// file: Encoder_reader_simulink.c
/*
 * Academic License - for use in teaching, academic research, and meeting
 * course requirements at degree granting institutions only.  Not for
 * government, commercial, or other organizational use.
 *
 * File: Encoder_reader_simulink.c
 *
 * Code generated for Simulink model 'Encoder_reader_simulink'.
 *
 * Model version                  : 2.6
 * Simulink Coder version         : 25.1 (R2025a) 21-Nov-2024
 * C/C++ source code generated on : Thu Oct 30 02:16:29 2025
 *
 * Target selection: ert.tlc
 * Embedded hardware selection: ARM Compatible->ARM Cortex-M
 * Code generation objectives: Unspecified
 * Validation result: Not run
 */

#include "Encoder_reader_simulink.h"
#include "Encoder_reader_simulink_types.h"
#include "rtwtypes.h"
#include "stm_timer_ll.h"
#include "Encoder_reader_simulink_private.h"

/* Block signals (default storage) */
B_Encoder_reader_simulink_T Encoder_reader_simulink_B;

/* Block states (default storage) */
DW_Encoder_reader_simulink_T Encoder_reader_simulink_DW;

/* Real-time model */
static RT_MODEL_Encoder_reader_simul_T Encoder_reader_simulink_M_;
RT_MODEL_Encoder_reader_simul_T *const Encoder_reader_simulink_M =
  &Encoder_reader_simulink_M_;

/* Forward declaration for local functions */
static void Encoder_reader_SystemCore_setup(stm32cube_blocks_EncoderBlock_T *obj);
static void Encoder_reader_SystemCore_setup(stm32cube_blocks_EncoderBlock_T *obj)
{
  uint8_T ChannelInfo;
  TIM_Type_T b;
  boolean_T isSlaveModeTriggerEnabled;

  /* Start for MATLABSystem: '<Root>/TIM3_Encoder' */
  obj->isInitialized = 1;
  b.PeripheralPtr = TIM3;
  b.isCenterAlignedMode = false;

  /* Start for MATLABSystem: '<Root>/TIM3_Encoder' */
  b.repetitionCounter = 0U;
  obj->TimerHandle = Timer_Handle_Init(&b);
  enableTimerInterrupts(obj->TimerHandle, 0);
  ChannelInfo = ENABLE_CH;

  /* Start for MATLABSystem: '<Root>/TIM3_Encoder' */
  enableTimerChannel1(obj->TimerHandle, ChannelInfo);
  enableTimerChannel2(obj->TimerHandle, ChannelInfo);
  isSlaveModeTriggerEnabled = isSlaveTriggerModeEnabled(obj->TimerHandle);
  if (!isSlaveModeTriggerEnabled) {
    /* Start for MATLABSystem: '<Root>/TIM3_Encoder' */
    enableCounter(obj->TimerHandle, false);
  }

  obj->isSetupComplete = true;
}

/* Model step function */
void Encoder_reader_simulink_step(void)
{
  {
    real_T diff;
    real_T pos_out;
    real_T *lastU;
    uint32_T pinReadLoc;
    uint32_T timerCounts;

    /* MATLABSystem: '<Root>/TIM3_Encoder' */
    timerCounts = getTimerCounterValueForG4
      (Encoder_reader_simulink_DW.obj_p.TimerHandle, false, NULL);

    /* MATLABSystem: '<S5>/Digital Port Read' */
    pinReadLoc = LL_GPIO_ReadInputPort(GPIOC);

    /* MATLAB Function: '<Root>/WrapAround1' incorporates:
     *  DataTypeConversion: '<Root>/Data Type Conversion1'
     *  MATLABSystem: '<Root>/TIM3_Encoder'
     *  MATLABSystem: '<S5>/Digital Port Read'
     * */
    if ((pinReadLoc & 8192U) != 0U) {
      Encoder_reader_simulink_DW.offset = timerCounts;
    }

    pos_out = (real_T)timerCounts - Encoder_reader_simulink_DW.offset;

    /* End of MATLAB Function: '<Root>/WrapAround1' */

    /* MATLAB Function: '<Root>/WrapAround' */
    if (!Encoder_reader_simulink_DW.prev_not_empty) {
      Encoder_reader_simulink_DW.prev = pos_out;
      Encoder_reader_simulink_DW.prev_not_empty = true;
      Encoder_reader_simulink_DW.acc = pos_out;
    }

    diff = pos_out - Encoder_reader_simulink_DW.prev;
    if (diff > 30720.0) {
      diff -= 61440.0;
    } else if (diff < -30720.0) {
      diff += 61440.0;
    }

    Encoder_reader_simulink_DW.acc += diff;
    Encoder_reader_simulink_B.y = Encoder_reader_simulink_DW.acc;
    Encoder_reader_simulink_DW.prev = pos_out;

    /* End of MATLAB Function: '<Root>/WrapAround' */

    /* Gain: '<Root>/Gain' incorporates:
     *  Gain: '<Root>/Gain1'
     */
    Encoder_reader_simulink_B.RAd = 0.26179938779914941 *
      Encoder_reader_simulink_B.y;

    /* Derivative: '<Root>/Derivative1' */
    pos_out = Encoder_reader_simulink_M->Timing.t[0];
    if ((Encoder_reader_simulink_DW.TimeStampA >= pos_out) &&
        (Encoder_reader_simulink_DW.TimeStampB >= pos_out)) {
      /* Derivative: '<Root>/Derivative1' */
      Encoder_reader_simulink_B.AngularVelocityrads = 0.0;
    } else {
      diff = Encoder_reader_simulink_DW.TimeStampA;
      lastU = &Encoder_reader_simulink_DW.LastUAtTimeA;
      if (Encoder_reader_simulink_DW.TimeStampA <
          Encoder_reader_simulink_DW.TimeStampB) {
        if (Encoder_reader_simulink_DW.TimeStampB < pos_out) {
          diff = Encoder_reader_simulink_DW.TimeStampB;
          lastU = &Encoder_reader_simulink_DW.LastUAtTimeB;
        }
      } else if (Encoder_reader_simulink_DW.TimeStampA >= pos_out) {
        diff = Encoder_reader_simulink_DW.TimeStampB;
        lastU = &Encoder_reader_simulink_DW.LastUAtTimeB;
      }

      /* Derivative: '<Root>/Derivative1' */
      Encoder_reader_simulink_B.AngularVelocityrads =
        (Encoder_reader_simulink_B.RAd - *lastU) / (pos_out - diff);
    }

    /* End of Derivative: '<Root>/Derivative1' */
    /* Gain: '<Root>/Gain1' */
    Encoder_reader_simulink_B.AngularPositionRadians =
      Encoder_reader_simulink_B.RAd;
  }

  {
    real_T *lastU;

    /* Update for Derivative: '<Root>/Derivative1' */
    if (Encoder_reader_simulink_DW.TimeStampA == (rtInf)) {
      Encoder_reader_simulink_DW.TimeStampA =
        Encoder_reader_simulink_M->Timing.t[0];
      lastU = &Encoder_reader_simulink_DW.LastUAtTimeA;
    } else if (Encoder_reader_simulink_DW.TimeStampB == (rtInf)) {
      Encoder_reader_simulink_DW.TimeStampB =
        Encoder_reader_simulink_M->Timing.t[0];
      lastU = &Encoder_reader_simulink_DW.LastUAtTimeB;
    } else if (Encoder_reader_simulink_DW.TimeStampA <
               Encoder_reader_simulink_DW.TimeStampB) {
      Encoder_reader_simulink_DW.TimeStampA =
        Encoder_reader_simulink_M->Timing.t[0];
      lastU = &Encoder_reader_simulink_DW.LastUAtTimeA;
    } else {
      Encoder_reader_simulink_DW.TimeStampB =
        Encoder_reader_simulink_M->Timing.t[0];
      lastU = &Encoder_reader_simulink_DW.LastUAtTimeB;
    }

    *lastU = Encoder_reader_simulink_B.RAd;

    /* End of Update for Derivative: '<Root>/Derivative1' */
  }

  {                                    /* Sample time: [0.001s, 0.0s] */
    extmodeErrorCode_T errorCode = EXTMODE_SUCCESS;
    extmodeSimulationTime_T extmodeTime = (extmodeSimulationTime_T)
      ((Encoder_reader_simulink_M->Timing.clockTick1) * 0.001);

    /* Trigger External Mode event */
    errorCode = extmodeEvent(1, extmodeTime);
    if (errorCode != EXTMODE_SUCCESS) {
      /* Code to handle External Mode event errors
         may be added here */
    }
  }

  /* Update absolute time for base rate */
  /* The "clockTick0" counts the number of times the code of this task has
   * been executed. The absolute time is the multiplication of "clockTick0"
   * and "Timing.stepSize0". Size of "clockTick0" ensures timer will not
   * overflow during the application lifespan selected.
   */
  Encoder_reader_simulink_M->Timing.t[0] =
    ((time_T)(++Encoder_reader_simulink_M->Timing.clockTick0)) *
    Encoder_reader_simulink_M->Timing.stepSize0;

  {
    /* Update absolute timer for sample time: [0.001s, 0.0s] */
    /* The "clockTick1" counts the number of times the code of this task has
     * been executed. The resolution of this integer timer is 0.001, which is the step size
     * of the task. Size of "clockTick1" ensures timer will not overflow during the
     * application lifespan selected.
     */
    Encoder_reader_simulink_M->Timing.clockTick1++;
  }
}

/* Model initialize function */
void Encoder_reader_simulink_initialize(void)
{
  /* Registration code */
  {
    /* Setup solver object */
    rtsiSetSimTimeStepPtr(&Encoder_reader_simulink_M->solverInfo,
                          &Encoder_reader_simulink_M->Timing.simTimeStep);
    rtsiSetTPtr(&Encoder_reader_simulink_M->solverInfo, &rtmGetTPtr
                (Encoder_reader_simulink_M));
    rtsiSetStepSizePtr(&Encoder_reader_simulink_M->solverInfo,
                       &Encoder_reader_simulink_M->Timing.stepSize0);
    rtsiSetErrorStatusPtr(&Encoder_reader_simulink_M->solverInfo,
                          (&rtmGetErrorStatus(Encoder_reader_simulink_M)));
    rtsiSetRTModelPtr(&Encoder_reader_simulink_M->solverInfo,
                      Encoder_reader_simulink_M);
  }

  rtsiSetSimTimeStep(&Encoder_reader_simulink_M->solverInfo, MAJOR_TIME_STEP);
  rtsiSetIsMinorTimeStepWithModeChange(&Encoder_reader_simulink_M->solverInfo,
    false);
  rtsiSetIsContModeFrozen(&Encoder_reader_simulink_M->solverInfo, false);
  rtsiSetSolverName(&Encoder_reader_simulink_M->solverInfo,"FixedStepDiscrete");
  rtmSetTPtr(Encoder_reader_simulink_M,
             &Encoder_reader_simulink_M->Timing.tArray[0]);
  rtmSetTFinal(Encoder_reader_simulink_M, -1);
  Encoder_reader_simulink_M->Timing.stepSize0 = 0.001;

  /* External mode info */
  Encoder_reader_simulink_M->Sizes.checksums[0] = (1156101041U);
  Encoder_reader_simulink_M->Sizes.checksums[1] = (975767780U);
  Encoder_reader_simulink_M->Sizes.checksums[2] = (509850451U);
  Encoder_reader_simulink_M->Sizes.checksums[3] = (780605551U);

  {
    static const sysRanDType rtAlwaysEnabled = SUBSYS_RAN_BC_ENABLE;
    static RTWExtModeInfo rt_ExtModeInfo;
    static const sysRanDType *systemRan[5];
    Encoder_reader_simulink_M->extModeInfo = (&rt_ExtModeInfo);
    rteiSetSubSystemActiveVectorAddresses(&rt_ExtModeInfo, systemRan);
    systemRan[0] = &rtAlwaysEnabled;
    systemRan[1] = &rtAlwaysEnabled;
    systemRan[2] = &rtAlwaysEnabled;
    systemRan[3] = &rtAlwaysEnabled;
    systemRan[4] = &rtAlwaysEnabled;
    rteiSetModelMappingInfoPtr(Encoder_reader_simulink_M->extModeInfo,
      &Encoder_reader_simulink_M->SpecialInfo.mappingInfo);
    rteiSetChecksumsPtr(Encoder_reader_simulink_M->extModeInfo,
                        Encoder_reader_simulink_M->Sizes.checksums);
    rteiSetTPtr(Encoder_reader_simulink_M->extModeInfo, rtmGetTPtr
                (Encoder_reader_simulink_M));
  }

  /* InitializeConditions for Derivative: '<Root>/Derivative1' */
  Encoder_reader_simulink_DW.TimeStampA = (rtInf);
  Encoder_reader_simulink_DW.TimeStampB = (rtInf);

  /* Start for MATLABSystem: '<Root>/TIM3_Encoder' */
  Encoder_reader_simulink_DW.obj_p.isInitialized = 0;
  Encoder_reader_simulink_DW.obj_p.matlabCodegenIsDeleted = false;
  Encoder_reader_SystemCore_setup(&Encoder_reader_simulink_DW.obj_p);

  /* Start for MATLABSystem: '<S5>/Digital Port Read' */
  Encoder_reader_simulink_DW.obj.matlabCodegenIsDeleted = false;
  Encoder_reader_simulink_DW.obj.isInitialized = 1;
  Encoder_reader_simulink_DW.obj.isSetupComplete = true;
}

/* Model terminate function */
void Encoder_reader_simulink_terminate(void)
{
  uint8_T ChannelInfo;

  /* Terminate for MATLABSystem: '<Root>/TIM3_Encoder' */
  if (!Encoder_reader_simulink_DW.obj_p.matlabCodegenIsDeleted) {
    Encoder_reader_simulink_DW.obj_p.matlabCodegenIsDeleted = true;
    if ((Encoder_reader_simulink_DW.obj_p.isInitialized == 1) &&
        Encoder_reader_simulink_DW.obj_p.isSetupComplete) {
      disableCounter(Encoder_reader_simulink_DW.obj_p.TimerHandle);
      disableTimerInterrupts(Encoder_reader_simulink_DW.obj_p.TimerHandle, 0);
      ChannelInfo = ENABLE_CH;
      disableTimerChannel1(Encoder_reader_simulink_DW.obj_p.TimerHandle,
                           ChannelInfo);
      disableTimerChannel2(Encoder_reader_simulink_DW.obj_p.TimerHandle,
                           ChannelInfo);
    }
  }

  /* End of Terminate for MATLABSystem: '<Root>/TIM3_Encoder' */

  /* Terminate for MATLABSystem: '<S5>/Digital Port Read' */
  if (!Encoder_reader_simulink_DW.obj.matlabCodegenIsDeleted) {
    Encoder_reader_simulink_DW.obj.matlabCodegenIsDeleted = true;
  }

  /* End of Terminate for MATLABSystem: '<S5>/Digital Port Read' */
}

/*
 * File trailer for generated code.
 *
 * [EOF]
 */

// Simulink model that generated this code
simulink model "Encoder_reader_simulink"  (R2025a)
settings: Solver=FixedStepAuto  StartTime=0.0  StopTime=inf  FixedStep=0.001  RelTol=1e-3  EnableMultiTasking=on
libraries: stm32f4xxblockslib x5, stm32g4xxblockslib x3

== system Encoder_reader_simulink ==
  Constant : Constant  Commented=on  Value=1.5
  Data Type Conversion1 : DataTypeConversion  OutDataTypeStr=double  SaturateOnIntegerOverflow=off  RndMeth=Floor
  Data Type Conversion2 : DataTypeConversion  Commented=on  OutDataTypeStr=double  SaturateOnIntegerOverflow=off  RndMeth=Floor
  Data Type Conversion3 : DataTypeConversion  Commented=on  OutDataTypeStr=double  SaturateOnIntegerOverflow=off  RndMeth=Floor
  Derivative1 : Derivative
  Digital Port Read1 : stm32f4xxblockslib/Digital Port Read  Commented=on  PortName=GPIOC  PinNumber=13  ReadOperation=on  IOAsArray=on  SampleTime=-1  EnableSimPort=off  hoistedMaskSrc=ECSoC/ECSimCodegen/Digital Port Read
  Digital Port Read2 : stm32f4xxblockslib/Digital Port Read  PortName=GPIOC  PinNumber=13  ReadOperation=on  IOAsArray=on  SampleTime=-1  EnableSimPort=off  hoistedMaskSrc=ECSoC/ECSimCodegen/Digital Port Read
  Digital Port Read3 : stm32f4xxblockslib/Digital Port Read  Commented=on  PortName=GPIOA  PinNumber=4  ReadOperation=on  IOAsArray=on  SampleTime=-1  EnableSimPort=off  hoistedMaskSrc=ECSoC/ECSimCodegen/Digital Port Read
  Digital Port Read4 : stm32f4xxblockslib/Digital Port Read  Commented=on  PortName=GPIOA  PinNumber=6  ReadOperation=on  IOAsArray=on  SampleTime=-1  EnableSimPort=off  hoistedMaskSrc=ECSoC/ECSimCodegen/Digital Port Read
  Digital Port Read5 : stm32f4xxblockslib/Digital Port Read  Commented=on  PortName=GPIOC  PinNumber=13  ReadOperation=on  IOAsArray=on  SampleTime=-1  EnableSimPort=off  hoistedMaskSrc=ECSoC/ECSimCodegen/Digital Port Read
  Display : Display
  Display{1..4} (4 alike) : Display  Commented=on
  Display5 : Display
  Display6 : Display
  Encoder : stm32g4xxblockslib/Encoder  Commented=on  TimerModule=TIM4  EnableResetInput=off  OutputCountAfterFirstIndex=off  OutputValidIndex=off  OutputDirection=off  OutputStatus=off  SampleTime=-1
  Gain : Gain  Gain=(2*pi)/24
  Gain1 : Gain  Gain=(2*pi)/24
  Sum : Sum  Commented=on  Inputs=|++
  TIM3_Encoder : stm32g4xxblockslib/Encoder  TimerModule=TIM3  EnableResetInput=off  OutputCountAfterFirstIndex=off  OutputValidIndex=off  OutputDirection=off  OutputStatus=off  SampleTime=-1
  TIM3_Encoder2 : stm32g4xxblockslib/Encoder  Commented=on  TimerModule=TIM1  EnableResetInput=off  OutputCountAfterFirstIndex=off  OutputValidIndex=off  OutputDirection=off  OutputStatus=off  SampleTime=-1
  WrapAround : MATLAB Function  TreatAsAtomicUnit=on
  WrapAround1 : MATLAB Function  TreatAsAtomicUnit=on
  WrapAround2 : MATLAB Function  Commented=on  TreatAsAtomicUnit=on
  WrapAround3 : MATLAB Function  Commented=on  TreatAsAtomicUnit=on
  WrapAround4 : MATLAB Function  Commented=on  TreatAsAtomicUnit=on
  WrapAround5 : MATLAB Function  Commented=on  TreatAsAtomicUnit=on
  wires:
  TIM3_Encoder/1 -> Data Type Conversion1/1
  WrapAround1/1(pos_out) -> WrapAround/1(u)
  Digital Port Read2/1 -> WrapAround1/2(home_btn)  "B"
  Data Type Conversion1/1 -> WrapAround1/1(pos_in)
  Data Type Conversion2/1 -> WrapAround3/1(pos_in)
  Digital Port Read1/1 -> WrapAround3/2(home_btn)  "B"
  WrapAround3/1(pos_out) -> WrapAround2/1(u)
  WrapAround2/1(y) -> Display1/1
  Encoder/1 -> Data Type Conversion2/1
  Digital Port Read3/1 -> Display2/1  "B"
  TIM3_Encoder2/1 -> Data Type Conversion3/1
  WrapAround4/1(y) -> Display4/1
  WrapAround5/1(pos_out) -> WrapAround4/1(u)
  Digital Port Read5/1 -> WrapAround5/2(home_btn)  "B"
  Data Type Conversion3/1 -> WrapAround5/1(pos_in)
  Digital Port Read4/1 -> Sum/1  "A"
  Constant/1 -> Sum/2
  Sum/1 -> Display3/1  "A"
  WrapAround/1(y) -> Display6/1, Gain1/1, Gain/1  "Relative Position (Pulses)"
  Gain/1 -> Derivative1/1  "RAd"
  Derivative1/1 -> Display/1  "Angular Velocity (rad/s)"
  Gain1/1 -> Display5/1  "Angular Position (Radians)"

== matlab function Encoder_reader_simulink/WrapAround1 ==
function pos_out = encoder_home(pos_in, home_btn)
%#codegen

persistent offset
if isempty(offset)
    offset = 0;  % ค่าเริ่มต้นของ offset
end

if home_btn == 1
    % เมื่อกดปุ่ม home ให้จำค่าปัจจุบันเป็น offset
    offset = pos_in;
end

% เอาค่าปัจจุบันลบด้วย offset → ให้ค่าเป็น 0 ที่ home
pos_out = pos_in - offset;

end

== matlab function Encoder_reader_simulink/WrapAround ==
function y = WrapAroundFcn(u)

persistent prev acc
if isempty(prev)
    prev = double(u);
    acc  = double(u);
end

wrapMax  = 61440;      % ค่า Period + 1 (61439 + 1)
halfWrap = wrapMax / 2;

% คำนวณความต่างระหว่างค่าปัจจุบันกับค่าก่อนหน้า
diff = double(u) - prev;

% ---------- ปรับค่าเมื่อข้ามรอบ ----------
if diff >  halfWrap
    % ข้ามจาก 61439 → 0  (CW)
    diff = diff - wrapMax;
elseif diff < -halfWrap
    % ข้ามจาก 0 → 61439  (CCW)
    diff = diff + wrapMax;
end

% ---------- สะสมค่าต่อเนื่อง ----------
acc = acc + diff;

% ---------- อัปเดตค่าและส่งออก ----------
y = acc;
prev = double(u);
end

== matlab function Encoder_reader_simulink/WrapAround2 ==
function y = WrapAroundFcn(u)

persistent prev acc
if isempty(prev)
    prev = double(u);
    acc  = double(u);
end

wrapMax  = 61440;      % ค่า Period + 1 (61439 + 1)
halfWrap = wrapMax / 2;

% คำนวณความต่างระหว่างค่าปัจจุบันกับค่าก่อนหน้า
diff = double(u) - prev;

% ---------- ปรับค่าเมื่อข้ามรอบ ----------
if diff >  halfWrap
    % ข้ามจาก 61439 → 0  (CW)
    diff = diff - wrapMax;
elseif diff < -halfWrap
    % ข้ามจาก 0 → 61439  (CCW)
    diff = diff + wrapMax;
end

% ---------- สะสมค่าต่อเนื่อง ----------
acc = acc + diff;

% ---------- อัปเดตค่าและส่งออก ----------
y = acc;
prev = double(u);
end

== matlab function Encoder_reader_simulink/WrapAround3 ==
function pos_out = encoder_home(pos_in, home_btn)
%#codegen

persistent offset
if isempty(offset)
    offset = 0;  % ค่าเริ่มต้นของ offset
end

if home_btn == 1
    % เมื่อกดปุ่ม home ให้จำค่าปัจจุบันเป็น offset
    offset = pos_in;
end

% เอาค่าปัจจุบันลบด้วย offset → ให้ค่าเป็น 0 ที่ home
pos_out = pos_in - offset;

end

== matlab function Encoder_reader_simulink/WrapAround4 ==
function y = WrapAroundFcn(u)

persistent prev acc
if isempty(prev)
    prev = double(u);
    acc  = double(u);
end

wrapMax  = 61440;      % ค่า Period + 1 (61439 + 1)
halfWrap = wrapMax / 2;

% คำนวณความต่างระหว่างค่าปัจจุบันกับค่าก่อนหน้า
diff = double(u) - prev;

% ---------- ปรับค่าเมื่อข้ามรอบ ----------
if diff >  halfWrap
    % ข้ามจาก 61439 → 0  (CW)
    diff = diff - wrapMax;
elseif diff < -halfWrap
    % ข้ามจาก 0 → 61439  (CCW)
    diff = diff + wrapMax;
end

% ---------- สะสมค่าต่อเนื่อง ----------
acc = acc + diff;

% ---------- อัปเดตค่าและส่งออก ----------
y = acc;
prev = double(u);
end

== matlab function Encoder_reader_simulink/WrapAround5 ==
function pos_out = encoder_home(pos_in, home_btn)
%#codegen

persistent offset
if isempty(offset)
    offset = 0;  % ค่าเริ่มต้นของ offset
end

if home_btn == 1
    % เมื่อกดปุ่ม home ให้จำค่าปัจจุบันเป็น offset
    offset = pos_in;
end

% เอาค่าปัจจุบันลบด้วย offset → ให้ค่าเป็น 0 ที่ home
pos_out = pos_in - offset;

end
